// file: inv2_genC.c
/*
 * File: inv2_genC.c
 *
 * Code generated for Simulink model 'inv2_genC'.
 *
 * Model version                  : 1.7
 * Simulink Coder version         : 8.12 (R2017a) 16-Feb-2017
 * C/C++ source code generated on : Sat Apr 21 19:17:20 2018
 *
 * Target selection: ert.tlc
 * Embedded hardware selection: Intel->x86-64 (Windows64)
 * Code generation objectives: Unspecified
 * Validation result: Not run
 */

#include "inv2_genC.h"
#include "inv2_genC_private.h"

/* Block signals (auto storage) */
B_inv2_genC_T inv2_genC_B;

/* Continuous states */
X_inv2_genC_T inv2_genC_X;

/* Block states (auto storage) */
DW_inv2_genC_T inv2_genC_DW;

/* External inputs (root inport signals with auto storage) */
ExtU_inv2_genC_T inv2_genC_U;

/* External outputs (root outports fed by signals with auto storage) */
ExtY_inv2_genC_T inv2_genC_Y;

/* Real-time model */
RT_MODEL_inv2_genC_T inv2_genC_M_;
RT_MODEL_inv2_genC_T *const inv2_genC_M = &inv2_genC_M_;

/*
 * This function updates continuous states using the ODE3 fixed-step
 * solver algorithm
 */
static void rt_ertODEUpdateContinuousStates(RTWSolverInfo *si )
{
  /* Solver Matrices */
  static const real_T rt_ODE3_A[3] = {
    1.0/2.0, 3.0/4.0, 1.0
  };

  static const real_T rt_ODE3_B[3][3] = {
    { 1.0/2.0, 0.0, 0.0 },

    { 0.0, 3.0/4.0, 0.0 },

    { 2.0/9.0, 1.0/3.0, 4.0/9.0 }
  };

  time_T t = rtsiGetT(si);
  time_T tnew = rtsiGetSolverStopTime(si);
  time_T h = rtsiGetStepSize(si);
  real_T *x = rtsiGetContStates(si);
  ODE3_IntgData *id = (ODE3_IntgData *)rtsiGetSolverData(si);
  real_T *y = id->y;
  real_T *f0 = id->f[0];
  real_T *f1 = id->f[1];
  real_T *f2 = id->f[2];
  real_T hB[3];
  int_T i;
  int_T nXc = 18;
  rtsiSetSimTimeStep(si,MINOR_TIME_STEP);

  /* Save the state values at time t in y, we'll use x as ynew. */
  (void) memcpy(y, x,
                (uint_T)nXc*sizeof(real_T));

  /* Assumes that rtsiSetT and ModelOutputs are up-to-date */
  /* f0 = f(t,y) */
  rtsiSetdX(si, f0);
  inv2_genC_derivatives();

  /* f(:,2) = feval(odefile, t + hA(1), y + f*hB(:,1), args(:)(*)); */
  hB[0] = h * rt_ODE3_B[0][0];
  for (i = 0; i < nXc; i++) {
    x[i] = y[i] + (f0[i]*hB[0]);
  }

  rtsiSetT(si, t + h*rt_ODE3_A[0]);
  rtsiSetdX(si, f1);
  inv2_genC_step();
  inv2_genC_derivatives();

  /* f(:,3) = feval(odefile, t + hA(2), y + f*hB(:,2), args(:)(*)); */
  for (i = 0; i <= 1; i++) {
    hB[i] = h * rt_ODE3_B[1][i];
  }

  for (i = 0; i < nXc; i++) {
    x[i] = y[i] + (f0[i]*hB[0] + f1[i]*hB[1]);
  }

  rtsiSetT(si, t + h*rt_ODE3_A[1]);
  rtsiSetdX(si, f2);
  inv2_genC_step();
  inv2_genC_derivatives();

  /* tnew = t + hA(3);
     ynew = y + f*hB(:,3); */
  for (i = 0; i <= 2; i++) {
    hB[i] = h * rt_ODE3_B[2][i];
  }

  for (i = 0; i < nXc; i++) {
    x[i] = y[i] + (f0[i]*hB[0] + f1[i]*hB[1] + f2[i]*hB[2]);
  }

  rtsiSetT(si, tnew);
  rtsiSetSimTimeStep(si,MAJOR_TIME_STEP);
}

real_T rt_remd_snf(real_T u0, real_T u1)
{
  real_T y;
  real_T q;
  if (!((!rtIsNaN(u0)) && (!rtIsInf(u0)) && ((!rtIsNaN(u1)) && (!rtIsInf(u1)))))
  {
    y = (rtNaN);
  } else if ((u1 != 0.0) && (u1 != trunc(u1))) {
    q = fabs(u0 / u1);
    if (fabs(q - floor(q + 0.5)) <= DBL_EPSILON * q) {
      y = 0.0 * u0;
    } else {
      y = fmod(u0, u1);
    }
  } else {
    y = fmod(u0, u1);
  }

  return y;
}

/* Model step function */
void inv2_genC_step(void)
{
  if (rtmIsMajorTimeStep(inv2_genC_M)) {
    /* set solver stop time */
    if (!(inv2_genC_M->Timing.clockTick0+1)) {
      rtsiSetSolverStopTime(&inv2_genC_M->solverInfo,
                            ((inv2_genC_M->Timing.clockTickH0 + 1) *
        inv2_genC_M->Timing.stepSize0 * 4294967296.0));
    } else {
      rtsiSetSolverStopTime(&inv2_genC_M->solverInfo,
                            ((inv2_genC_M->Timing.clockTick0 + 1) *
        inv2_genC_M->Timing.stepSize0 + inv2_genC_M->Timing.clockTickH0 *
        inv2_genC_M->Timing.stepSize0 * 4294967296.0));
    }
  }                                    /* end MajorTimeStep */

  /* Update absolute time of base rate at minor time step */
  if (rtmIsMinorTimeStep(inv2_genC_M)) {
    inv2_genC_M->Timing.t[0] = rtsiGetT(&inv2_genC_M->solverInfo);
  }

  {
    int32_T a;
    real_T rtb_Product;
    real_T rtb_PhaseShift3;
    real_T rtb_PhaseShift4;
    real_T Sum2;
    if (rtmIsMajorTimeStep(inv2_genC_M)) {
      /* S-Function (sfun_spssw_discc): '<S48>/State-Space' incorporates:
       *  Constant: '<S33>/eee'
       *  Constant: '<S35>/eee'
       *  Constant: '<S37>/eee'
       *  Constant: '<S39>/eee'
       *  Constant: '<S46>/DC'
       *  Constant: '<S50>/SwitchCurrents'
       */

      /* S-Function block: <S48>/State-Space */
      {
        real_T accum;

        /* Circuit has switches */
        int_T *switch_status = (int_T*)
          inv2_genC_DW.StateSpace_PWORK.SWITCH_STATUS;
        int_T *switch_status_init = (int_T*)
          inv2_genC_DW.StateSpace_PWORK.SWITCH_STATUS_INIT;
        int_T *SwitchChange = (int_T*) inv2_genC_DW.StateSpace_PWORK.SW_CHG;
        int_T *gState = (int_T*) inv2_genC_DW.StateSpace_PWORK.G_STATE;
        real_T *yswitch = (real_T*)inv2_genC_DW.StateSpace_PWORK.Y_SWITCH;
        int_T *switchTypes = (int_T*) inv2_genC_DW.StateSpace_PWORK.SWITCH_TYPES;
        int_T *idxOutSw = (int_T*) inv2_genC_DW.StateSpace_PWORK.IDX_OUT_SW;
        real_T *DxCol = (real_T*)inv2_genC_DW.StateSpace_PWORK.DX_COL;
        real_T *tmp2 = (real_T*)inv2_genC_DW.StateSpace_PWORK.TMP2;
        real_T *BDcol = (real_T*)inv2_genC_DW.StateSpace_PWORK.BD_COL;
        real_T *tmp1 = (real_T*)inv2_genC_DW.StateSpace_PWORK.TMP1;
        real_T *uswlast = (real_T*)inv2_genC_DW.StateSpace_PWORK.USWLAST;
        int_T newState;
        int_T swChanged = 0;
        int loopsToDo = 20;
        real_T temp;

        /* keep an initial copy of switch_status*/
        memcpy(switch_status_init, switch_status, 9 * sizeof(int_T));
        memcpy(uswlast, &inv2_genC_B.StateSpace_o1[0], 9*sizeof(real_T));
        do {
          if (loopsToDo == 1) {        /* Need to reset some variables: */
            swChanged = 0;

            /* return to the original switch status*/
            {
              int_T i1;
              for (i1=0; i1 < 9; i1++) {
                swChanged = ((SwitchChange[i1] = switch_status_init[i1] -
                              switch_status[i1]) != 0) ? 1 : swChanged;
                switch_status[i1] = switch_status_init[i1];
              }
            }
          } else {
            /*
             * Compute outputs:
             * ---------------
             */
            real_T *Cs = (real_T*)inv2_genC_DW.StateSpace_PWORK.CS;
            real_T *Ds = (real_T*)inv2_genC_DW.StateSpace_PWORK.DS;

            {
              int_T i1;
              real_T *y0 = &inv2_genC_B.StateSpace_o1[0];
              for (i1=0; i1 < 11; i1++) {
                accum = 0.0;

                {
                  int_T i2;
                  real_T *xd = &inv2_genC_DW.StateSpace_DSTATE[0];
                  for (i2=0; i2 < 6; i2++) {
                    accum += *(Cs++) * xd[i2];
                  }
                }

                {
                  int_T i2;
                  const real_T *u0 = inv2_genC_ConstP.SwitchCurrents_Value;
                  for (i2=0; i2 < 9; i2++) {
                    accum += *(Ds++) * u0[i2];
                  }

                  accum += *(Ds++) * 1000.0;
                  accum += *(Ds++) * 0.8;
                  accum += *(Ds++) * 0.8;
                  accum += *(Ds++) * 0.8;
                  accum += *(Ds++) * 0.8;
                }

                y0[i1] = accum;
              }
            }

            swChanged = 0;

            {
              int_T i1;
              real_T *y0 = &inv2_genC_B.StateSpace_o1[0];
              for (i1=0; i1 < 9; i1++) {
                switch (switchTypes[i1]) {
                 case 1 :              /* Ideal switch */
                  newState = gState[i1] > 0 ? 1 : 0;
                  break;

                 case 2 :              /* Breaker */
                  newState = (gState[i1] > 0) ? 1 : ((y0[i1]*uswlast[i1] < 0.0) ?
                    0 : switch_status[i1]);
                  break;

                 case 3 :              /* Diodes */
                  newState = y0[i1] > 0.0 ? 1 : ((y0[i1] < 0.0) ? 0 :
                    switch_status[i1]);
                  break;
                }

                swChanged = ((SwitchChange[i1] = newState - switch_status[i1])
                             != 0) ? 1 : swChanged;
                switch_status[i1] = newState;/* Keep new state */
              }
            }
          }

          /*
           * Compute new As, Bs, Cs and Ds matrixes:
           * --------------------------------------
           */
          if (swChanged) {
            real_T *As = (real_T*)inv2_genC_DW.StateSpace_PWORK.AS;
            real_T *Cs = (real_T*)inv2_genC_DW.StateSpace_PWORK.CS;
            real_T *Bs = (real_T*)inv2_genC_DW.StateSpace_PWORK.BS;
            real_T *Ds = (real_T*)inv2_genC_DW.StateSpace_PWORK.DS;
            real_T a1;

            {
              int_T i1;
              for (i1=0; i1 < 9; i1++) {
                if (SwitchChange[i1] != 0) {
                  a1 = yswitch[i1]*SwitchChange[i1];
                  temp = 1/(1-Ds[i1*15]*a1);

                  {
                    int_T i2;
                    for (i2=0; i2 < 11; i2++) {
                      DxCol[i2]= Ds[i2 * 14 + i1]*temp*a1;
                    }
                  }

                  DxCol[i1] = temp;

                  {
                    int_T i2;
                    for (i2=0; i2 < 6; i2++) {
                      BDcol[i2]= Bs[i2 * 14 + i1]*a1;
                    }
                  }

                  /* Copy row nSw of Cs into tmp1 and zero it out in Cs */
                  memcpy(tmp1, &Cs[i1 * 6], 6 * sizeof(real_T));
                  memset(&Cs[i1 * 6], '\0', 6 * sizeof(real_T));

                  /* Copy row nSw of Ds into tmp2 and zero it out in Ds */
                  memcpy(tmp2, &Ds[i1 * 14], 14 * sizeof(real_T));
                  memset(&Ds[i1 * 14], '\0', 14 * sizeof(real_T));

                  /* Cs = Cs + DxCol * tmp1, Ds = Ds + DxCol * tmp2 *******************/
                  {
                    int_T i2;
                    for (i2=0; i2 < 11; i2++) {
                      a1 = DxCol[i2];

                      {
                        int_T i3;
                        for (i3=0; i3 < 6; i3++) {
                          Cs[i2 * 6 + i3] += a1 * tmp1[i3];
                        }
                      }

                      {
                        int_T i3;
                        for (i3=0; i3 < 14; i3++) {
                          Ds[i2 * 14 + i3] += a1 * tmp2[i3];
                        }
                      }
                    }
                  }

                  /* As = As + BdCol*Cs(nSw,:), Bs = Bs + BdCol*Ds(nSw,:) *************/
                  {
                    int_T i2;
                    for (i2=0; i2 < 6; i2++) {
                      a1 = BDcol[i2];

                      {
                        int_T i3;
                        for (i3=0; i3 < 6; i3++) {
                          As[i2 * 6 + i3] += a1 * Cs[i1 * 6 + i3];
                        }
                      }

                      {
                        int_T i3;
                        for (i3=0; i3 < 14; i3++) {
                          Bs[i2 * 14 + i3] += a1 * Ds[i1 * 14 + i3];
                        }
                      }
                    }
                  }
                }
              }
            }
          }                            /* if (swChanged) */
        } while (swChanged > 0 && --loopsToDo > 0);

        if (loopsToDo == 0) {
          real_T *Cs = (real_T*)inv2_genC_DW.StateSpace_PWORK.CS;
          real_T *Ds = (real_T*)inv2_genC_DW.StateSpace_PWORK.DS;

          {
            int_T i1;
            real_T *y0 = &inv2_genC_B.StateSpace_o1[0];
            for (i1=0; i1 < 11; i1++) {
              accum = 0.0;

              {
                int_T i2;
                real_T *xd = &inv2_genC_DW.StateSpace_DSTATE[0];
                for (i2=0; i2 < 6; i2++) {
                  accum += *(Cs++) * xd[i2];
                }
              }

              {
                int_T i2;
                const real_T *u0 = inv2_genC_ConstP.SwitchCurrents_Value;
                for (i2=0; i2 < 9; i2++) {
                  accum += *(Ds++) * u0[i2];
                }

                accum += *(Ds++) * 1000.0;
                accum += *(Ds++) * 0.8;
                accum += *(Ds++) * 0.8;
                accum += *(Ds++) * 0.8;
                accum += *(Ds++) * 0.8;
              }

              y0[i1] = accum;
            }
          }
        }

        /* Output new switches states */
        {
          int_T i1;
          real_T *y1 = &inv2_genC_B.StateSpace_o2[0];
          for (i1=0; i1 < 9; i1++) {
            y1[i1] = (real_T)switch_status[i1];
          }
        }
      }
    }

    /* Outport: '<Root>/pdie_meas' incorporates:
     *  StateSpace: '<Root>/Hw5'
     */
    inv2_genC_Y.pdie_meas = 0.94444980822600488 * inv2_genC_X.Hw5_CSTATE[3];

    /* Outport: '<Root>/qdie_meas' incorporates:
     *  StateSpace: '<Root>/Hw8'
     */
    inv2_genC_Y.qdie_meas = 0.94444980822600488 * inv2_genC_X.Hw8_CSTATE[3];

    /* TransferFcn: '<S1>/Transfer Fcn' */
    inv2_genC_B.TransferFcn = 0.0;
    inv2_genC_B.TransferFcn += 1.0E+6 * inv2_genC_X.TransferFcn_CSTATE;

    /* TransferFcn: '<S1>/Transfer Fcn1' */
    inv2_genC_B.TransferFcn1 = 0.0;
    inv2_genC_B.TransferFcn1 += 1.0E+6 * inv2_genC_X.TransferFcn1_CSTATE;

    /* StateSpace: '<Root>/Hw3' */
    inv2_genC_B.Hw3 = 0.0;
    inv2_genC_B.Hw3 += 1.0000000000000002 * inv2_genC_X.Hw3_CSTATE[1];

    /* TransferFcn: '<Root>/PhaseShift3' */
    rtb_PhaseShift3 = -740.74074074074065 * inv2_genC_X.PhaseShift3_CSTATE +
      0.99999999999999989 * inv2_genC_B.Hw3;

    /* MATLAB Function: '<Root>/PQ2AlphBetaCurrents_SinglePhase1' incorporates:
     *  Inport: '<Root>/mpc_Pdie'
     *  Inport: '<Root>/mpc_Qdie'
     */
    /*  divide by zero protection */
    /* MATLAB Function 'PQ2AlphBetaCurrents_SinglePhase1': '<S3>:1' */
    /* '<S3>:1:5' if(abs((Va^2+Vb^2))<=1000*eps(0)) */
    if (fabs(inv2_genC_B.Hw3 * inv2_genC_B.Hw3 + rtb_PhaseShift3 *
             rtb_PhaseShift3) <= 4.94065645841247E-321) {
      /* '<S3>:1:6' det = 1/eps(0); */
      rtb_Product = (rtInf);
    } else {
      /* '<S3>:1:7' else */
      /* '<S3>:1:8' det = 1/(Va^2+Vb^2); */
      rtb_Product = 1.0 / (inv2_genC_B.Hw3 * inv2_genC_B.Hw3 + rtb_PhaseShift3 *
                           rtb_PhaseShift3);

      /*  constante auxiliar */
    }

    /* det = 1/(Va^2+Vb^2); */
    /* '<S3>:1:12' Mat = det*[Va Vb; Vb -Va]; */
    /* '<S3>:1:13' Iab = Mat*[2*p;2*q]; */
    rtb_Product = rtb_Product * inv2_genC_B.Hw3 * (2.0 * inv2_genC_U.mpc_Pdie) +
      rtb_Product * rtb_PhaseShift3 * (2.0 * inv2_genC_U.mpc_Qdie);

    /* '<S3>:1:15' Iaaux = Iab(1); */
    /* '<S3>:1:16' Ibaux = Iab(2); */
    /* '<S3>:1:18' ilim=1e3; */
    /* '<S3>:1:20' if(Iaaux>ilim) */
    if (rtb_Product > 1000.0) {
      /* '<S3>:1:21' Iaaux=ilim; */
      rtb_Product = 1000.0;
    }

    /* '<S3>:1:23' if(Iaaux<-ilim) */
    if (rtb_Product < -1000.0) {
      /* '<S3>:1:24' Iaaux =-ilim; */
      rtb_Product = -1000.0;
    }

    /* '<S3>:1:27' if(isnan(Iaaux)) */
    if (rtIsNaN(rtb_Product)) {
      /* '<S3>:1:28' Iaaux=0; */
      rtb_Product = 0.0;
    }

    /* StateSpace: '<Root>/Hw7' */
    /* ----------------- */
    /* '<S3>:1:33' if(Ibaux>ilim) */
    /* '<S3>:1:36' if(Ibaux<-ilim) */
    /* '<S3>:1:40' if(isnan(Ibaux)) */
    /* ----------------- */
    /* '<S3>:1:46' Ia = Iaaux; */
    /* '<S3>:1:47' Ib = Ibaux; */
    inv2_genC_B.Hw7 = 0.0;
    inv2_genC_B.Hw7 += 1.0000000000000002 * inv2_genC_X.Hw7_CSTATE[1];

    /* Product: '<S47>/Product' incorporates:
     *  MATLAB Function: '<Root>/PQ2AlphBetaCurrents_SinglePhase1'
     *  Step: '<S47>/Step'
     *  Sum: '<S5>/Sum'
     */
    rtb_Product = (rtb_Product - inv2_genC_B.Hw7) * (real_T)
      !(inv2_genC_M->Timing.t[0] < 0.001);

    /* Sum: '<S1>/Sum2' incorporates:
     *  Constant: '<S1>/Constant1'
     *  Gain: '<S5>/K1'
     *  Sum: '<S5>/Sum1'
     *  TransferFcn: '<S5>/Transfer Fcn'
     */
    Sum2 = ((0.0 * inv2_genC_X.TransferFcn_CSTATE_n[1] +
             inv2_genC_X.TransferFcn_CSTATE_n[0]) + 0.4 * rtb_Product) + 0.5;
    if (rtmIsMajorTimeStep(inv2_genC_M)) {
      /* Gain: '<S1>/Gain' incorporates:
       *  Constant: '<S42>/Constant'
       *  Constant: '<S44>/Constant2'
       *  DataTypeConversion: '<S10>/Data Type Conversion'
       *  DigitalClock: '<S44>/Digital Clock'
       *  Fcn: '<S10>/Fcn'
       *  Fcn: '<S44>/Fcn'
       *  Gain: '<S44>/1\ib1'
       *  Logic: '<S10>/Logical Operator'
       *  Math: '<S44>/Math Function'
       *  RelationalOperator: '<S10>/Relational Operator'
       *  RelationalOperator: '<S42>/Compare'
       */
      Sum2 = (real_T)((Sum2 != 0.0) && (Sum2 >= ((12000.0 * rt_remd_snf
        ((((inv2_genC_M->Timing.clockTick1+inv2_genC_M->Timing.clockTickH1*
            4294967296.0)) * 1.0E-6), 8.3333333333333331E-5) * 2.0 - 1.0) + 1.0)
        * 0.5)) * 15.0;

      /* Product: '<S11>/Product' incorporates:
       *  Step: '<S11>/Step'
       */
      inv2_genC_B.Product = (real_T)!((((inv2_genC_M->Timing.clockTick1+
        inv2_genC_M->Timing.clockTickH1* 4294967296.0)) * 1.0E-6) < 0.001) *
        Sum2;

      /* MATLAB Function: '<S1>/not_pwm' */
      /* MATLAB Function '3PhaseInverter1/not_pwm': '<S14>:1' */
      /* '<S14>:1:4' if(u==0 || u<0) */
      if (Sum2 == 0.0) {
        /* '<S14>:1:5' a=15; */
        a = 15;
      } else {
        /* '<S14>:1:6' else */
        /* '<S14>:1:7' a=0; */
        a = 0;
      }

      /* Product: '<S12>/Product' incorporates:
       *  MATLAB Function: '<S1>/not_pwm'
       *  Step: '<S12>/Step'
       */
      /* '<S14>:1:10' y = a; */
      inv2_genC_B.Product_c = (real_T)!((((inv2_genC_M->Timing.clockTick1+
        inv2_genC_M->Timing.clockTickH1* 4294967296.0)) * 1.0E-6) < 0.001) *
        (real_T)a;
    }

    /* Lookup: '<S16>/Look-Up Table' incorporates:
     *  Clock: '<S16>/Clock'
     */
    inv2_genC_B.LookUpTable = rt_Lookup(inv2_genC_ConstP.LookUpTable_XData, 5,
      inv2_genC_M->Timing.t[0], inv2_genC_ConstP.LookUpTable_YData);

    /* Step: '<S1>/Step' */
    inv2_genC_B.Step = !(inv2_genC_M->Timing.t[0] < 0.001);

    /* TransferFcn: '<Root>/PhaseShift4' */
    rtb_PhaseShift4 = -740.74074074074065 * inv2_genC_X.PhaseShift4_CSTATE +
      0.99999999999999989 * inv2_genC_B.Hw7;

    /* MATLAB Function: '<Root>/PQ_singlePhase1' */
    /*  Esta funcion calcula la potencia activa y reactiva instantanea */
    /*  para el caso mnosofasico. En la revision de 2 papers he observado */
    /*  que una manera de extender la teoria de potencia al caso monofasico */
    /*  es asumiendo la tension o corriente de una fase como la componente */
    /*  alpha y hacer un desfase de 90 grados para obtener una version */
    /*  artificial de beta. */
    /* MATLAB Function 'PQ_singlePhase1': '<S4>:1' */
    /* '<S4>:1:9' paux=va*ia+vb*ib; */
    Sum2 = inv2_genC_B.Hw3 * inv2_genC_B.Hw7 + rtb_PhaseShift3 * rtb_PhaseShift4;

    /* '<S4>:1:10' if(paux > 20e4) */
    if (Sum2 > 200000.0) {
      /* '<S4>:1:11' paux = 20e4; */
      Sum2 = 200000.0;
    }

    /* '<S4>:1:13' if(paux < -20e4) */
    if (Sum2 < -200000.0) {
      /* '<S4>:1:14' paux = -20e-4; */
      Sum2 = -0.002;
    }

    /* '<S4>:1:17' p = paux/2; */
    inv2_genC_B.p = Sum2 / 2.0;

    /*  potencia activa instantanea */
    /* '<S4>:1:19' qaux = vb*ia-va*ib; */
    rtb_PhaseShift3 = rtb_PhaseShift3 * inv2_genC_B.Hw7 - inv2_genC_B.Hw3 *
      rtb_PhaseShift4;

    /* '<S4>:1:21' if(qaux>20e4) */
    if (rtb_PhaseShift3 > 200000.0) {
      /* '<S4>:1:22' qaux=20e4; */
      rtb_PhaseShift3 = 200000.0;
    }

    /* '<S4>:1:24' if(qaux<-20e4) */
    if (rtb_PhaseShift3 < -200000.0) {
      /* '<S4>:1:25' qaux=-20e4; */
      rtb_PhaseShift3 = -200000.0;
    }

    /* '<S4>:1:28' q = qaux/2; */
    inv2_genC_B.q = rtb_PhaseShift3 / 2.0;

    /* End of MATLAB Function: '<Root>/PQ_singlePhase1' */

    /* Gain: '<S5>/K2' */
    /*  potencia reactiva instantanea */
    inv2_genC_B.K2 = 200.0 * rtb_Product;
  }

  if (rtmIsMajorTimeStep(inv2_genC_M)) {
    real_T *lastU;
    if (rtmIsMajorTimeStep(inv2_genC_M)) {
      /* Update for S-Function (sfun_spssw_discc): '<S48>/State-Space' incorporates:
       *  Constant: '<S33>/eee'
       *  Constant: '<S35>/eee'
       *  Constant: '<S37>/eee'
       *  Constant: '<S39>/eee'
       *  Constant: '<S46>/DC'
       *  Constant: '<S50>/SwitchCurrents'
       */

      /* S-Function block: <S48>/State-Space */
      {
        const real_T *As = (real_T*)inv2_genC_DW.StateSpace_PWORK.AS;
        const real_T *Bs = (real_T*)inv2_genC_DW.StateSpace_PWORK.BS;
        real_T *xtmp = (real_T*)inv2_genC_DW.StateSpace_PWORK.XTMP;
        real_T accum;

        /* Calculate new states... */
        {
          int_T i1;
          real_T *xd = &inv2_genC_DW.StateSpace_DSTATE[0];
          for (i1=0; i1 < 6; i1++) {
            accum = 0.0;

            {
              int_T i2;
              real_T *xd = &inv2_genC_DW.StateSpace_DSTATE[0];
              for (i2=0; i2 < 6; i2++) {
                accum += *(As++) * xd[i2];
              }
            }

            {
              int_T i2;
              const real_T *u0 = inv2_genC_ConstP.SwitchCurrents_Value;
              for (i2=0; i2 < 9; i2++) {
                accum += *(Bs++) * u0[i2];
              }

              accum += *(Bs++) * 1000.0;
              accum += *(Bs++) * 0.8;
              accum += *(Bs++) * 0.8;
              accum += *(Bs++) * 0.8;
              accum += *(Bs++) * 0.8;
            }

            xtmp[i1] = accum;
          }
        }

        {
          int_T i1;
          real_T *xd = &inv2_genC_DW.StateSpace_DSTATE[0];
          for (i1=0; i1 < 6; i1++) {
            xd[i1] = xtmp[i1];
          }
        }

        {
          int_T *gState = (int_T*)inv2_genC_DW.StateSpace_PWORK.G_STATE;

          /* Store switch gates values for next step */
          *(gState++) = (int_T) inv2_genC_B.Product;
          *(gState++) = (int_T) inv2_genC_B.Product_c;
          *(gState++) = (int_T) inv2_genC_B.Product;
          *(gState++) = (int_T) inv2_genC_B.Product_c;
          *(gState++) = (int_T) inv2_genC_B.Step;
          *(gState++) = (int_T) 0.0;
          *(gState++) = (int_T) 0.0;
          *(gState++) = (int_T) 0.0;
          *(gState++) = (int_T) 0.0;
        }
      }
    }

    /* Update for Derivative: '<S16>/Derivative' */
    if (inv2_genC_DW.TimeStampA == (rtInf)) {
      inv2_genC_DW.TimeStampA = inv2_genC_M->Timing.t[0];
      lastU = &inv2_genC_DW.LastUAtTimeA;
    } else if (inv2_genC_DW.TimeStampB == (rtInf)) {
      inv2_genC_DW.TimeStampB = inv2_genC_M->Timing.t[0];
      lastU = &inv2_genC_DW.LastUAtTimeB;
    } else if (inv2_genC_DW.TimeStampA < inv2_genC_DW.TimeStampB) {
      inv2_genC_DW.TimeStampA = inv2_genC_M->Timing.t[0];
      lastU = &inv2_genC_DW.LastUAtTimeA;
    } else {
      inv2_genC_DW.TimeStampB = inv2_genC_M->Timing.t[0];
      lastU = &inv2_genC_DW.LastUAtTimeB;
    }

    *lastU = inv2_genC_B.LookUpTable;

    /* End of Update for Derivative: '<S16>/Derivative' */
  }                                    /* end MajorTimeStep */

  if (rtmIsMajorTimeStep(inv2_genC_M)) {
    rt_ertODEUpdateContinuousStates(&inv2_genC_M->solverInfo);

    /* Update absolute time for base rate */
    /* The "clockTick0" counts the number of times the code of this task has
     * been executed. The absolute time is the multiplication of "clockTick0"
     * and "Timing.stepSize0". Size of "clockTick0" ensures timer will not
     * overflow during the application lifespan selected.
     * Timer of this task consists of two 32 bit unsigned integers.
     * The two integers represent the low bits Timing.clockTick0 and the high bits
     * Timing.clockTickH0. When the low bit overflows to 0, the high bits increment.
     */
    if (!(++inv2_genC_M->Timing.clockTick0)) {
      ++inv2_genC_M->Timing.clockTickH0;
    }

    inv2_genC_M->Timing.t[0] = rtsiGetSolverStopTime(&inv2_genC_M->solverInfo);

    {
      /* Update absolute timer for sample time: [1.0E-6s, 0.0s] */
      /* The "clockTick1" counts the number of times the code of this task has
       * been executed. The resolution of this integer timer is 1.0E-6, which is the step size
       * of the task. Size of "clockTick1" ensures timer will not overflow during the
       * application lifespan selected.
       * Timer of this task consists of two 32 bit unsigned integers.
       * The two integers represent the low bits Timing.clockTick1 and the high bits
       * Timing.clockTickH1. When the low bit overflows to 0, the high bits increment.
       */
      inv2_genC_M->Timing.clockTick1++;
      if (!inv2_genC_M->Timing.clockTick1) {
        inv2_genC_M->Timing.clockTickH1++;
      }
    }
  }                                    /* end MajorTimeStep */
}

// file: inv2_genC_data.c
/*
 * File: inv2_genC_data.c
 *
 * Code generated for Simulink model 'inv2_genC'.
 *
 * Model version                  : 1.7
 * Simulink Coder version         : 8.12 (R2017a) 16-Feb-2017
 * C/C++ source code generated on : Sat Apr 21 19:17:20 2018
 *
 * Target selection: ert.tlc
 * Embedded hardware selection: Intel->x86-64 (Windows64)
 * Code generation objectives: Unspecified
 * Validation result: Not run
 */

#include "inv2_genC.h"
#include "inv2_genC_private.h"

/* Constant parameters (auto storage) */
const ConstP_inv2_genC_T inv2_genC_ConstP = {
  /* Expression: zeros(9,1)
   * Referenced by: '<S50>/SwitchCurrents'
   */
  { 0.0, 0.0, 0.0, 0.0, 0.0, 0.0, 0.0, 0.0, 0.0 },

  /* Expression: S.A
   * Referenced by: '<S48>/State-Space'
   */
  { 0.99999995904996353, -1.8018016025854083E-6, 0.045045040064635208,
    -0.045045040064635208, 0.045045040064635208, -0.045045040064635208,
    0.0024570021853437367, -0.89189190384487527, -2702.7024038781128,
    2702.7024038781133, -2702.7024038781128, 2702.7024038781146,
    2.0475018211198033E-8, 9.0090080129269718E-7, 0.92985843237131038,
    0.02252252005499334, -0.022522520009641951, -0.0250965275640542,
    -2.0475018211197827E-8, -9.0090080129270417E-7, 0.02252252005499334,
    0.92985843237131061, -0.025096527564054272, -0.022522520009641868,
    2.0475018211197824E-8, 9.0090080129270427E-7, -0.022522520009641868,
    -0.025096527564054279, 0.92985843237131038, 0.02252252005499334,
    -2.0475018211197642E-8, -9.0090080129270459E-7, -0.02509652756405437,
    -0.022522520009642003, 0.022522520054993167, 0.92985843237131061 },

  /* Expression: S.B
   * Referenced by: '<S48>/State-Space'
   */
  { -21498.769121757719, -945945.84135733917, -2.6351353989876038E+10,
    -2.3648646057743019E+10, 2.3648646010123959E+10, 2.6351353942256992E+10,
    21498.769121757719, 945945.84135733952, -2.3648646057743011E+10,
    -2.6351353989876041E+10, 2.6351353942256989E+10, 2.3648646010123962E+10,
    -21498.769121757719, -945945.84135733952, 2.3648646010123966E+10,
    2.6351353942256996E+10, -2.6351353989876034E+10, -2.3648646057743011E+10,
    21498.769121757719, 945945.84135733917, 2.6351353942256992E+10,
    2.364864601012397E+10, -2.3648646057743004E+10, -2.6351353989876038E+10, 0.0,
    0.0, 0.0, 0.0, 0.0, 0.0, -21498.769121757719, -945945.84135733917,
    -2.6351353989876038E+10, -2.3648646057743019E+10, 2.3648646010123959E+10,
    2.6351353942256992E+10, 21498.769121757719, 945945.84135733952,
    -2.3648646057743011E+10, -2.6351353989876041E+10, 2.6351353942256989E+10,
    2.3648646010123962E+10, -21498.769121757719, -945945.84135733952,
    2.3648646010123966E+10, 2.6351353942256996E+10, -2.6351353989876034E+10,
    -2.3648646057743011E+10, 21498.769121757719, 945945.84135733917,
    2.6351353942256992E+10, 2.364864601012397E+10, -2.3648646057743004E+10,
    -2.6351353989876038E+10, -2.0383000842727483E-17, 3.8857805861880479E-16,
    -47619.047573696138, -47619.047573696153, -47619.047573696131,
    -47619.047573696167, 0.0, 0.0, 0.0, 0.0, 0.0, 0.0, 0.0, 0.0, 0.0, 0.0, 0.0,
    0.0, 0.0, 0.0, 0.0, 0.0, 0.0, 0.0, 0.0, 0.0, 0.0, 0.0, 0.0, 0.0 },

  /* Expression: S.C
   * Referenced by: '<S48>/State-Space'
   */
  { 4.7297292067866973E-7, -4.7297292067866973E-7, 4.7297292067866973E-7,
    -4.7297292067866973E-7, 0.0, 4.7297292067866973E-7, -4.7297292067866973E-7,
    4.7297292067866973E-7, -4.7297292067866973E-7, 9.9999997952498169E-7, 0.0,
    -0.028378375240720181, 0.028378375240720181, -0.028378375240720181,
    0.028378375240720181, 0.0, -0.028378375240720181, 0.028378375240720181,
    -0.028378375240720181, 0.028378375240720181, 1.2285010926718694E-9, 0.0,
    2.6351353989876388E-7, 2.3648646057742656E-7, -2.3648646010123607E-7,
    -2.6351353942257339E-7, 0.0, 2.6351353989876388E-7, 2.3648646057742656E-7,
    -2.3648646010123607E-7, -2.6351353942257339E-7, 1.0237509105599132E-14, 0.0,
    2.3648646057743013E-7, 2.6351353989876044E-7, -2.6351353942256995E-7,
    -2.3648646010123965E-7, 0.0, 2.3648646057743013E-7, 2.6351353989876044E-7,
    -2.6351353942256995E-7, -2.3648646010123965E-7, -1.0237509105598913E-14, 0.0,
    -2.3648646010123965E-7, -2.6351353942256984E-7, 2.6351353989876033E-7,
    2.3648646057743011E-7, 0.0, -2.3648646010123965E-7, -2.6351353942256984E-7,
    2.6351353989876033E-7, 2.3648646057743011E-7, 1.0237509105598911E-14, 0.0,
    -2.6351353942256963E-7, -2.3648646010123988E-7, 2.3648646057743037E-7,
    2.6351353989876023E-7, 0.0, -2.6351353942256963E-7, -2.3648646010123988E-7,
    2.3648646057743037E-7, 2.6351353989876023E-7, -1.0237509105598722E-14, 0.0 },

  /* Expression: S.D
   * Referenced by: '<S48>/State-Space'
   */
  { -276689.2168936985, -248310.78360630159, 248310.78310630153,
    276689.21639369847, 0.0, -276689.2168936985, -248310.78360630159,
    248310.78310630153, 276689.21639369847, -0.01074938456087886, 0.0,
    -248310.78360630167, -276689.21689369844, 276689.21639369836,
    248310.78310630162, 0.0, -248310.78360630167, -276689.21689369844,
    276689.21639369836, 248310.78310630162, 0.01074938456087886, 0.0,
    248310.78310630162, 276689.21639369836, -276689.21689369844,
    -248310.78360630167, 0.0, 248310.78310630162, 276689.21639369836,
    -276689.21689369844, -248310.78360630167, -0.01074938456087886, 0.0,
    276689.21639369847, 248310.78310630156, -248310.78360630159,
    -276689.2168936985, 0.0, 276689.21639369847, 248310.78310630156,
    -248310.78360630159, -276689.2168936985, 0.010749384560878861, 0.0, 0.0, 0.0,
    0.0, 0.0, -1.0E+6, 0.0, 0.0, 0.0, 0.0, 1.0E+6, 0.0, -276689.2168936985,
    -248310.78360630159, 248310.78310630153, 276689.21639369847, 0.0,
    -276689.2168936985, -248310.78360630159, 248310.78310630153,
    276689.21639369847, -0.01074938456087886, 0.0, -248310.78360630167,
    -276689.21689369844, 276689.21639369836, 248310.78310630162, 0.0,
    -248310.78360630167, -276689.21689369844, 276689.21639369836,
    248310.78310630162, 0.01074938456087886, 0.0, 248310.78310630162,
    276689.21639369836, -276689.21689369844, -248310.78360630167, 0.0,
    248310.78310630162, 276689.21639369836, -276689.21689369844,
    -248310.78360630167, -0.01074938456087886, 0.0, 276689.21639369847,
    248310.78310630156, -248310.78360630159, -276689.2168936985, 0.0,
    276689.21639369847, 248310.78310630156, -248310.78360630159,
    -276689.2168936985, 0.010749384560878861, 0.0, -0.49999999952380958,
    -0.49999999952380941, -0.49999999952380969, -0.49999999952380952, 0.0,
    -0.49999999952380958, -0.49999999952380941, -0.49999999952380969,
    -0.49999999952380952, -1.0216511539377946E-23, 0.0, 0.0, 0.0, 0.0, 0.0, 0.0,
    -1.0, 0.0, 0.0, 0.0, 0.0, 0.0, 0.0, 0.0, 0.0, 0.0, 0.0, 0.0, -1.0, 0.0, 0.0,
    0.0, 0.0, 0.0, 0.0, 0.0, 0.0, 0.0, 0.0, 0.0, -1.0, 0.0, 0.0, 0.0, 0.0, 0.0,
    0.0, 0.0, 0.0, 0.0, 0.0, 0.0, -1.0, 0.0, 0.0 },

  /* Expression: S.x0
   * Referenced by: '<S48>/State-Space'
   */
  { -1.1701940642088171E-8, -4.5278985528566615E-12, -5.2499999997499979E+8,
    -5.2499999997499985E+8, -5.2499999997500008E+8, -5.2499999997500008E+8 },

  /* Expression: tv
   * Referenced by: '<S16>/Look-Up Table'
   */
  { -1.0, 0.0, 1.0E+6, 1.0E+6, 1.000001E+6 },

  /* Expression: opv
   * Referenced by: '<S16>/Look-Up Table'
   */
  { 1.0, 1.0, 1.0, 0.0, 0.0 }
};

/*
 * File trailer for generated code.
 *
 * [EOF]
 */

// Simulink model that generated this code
simulink model "inv2_genC"  (R2017a)
settings: Solver=ode3  StartTime=0.0  StopTime=10.0  FixedStep=1e-6  MaxStep=1e-4  RelTol=1e-3
libraries: powerlib x17, dsparch4 x4, powerlib_meascontrol x1

== system inv2_genC ==
  note: DIESEL - CSI
  mpc_Pdie : Inport
  mpc_Qdie : Inport  Port=2
  3PhaseInverter1 : Subsystem  mask{st_time=1e-3, f_sw=12000, samp_f=1e-6}
      mask prompts: st_time "Tiempo muerto (Start)"; f_sw "Switching frequency"; samp_f "Sampling frequency"
  DC_2 : powerlib/Electrical Sources/DC Voltage Source  Amplitude=1000  Measurements=None
  Ground3 : powerlib/Elements/Ground  LConnTagsString=a
  Hw3 : dsparch4/Analog Filter Design  method=Bessel  filttype=Lowpass  N=2  Wlo=7000*2*pi  Whi=80  Rp=2  Rs=80
  Hw5 : dsparch4/Analog Filter Design  method=Bessel  filttype=Lowpass  N=4  Wlo=30*2*pi  Whi=80  Rp=2  Rs=80
  Hw7 : dsparch4/Analog Filter Design  method=Bessel  filttype=Lowpass  N=2  Wlo=7000*2*pi  Whi=80  Rp=2  Rs=80
  Hw8 : dsparch4/Analog Filter Design  method=Bessel  filttype=Lowpass  N=4  Wlo=30*2*pi  Whi=80  Rp=2  Rs=80
  PQ2AlphBetaCurrents_SinglePhase1 : MATLAB Function  TreatAsAtomicUnit=on
  PQ_singlePhase1 : MATLAB Function  TreatAsAtomicUnit=on
  PR Controller_0_ref 2 : Subsystem  mask{Kp=40/100, Ki=200, wa=2, w0=60*2*pi, st_time=1e-3}
      mask prompts: Kp "Ganancia Proporcional"; Ki "Ganancia Integral"; wa "Ancho camapana resonancia"; w0 "Frecuencia Central"; st_time "Tiempo muerto (Start)"
  PhaseShift3 : TransferFcn  Numerator=[2.7e-3 -1]  Denominator=[2.7e-3 1]
  PhaseShift4 : TransferFcn  Numerator=[2.7e-3 -1]  Denominator=[2.7e-3 1]
  Rin1 : powerlib/Elements/Series RLC Branch  LConnTagsString=__new0  RConnTagsString=__new0  BranchType=R  Resistance=.001  Inductance=0  SetiL0=off  InitialCurrent=0  Capacitance=0  Setx0=off  InitialVoltage=0  Measurements=None
  Scope1 : Scope  NumInputPorts=2
  Scope3 : Scope  NumInputPorts=2
  powergui : powerlib/powergui  Priority=1  SimulationMode=Discrete  SampleTime=1e-6  frequency=60  Iterations=50  frequencyindice=0  Pbase=100e6  ErrMax=1e-4  UnitsV=kV  UnitsW=MW  buscounter=0  FunctionMessages=off  echomessages=off  EnableUseOfTLC=off  CurrentSourceSwitches=off  DisableSnubberDevices=off  DisableRonSwitches=off  DisableVfSwitches=off  DisplayEquations=off  SolverType=Tustin/Backward Euler (TBE)  Interpol=off  ExternalGateDelay=off  methode=off  Ts=100  x0status=blocks  SPID=on  SwTol=0  HookPort=off  RestoreLinks=warning  ResistiveCurrentMeasurement=off  Frange=[0:2:500]  Ylog=off  Xlog=on  ShowGrid=off  save=off  variable=ZData  structure=0  ZoomFFT=off  StartTime=0.0  cycles=1  DisplayStyle=1  fundamental=60  FreqAxis=off  MaxFrequency=1000  frequencyindicesteady=1  RmsSteady=1  display=off
  pdie_meas : Outport
  qdie_meas : Outport  Port=2
  wires:
  3PhaseInverter1/1(Iout) -> Hw7/1
  [D_die] -> 3PhaseInverter1/1(A_in)
  PQ2AlphBetaCurrents_SinglePhase1/1(Ia) -> [Ia_ref_die]
  [I_die] -> PhaseShift4/1, [I_alf_die]
  Hw7/1 -> [I_die]
  [V_alf_die] -> PQ2AlphBetaCurrents_SinglePhase1/1(Va)
  PhaseShift4/1 -> [I_bet_die]
  PhaseShift3/1 -> [V_bet_die]
  [Ia_ref_die] -> PR Controller_0_ref 2/1(ref), Scope1/1
  [V_die] -> Scope3/2
  Hw3/1 -> [V_die]
  3PhaseInverter1/2(Vout) -> Hw3/1
  [I_die] -> PR Controller_0_ref 2/2(real), Scope1/2
  PR Controller_0_ref 2/1(Out1) -> [D_die]
  [V_die] -> [V_alf_die], PhaseShift3/1
  [I_die] -> Scope3/1
  [V_bet_die] -> PQ2AlphBetaCurrents_SinglePhase1/2(Vb)
  PQ_singlePhase1/1(p) -> Hw5/1
  PQ_singlePhase1/2(q) -> Hw8/1
  [I_bet_die] -> PQ_singlePhase1/4(ib)
  [V_bet_die] -> PQ_singlePhase1/2(vb)
  [V_alf_die] -> PQ_singlePhase1/1(va)
  Hw8/1 -> qdie_meas/1
  [I_alf_die] -> PQ_singlePhase1/3(ia)
  Hw5/1 -> pdie_meas/1
  mpc_Pdie/1 -> PQ2AlphBetaCurrents_SinglePhase1/3(p)
  mpc_Qdie/1 -> PQ2AlphBetaCurrents_SinglePhase1/4(q)
  connections:
  DC_2/RConn1 -- Rin1/LConn1
  3PhaseInverter1/RConn2 -- Ground3/LConn1
  Rin1/RConn1 -- 3PhaseInverter1/LConn1
  DC_2/LConn1 -- 3PhaseInverter1/LConn2

== system inv2_genC/3PhaseInverter1 ==
  note: Gate Drivers: Generan las señales cuadradas para
      | la conmutacion del convertidor de 3 brazos e implementan el
      | tiempo muerto para mejorar la calidad de la simulacion
  A_in : Inport
  Breaker : powerlib/Elements/Breaker  InitialState=0  SwitchingTimes="[1/60  5/60]"  External=on  BreakerResistance=0.01  SnubberResistance=1e6  SnubberCapacitance=inf  Measurements=None  MoreParameters=on  NoBreakLoop=off
  Cf : powerlib/Elements/Series RLC Branch  LConnTagsString=__new0  RConnTagsString=__new0  BranchType=C  Resistance=1  Inductance=1e-3  SetiL0=off  InitialCurrent=0  Capacitance=22e-6  Setx0=off  InitialVoltage=0  Measurements=None
  Constant1 : Constant  Value=0.5
  Gain : Gain  Gain=15
  H bridge : Subsystem
  I sens A : powerlib/Measurements/Current Measurement  PhasorSimulation=off  OutputType=Complex  PSBequivalent=0
  Lf : powerlib/Elements/Series RLC Branch  LConnTagsString=__new0  RConnTagsString=__new0  BranchType=RL  Resistance=.1  Inductance=30e-3  SetiL0=off  InitialCurrent=0  Capacitance=1e-6  Setx0=off  InitialVoltage=0  Measurements=None
  PWM Generator (DC-DC) : powerlib_meascontrol/Pulse & Signal Generators/PWM Generator (DC-DC)  Fsw=f_sw  Ts=samp_f
  Step : Step  Time=st_time  SampleTime=0
  Steper1 : Subsystem
  Steper3 : Subsystem
  Sum2 : Sum
  Transfer Fcn : TransferFcn  Denominator=[1e-6 1]
  Transfer Fcn1 : TransferFcn  Denominator=[1e-6 1]
  Vsensa1 : powerlib/Measurements/Voltage Measurement  PhasorSimulation=off  OutputType=Complex  PSBequivalent=0
  not_pwm : MATLAB Function  TreatAsAtomicUnit=on
  Vout+ : PMIOPort  Port=1  Side=Right
  Vout- : PMIOPort  Port=2  Side=Right
  Collector : PMIOPort  Port=3  Side=Left
  Emitter : PMIOPort  Port=4  Side=Left
  Iout : Outport
  Vout : Outport  Port=2
  wires:
  Vsensa1/1 -> Transfer Fcn1/1  "A_volts"
  I sens A/1 -> Transfer Fcn/1  "A_current"
  [pwma] -> H bridge/4(Blo)
  [Npwma] -> H bridge/3(Alo), H bridge/2(Bhi)
  [pwma] -> H bridge/1(Ahi)
  Gain/1 -> not_pwm/1(u), Steper1/1(In1)
  Steper3/1(Out1) -> [Npwma]
  Steper1/1(Out1) -> [pwma]
  A_in/1 -> Sum2/1
  Constant1/1 -> Sum2/2
  PWM Generator (DC-DC)/1 -> Gain/1
  Sum2/1 -> PWM Generator (DC-DC)/1
  not_pwm/1(y) -> Steper3/1(In1)
  Transfer Fcn/1 -> Iout/1
  Transfer Fcn1/1 -> Vout/1
  Step/1 -> Breaker/1
  connections:
  Cf/RConn1 -- Vsensa1/LConn2 -- Vout-/RConn1 -- H bridge/RConn2
  Lf/LConn1 -- H bridge/RConn1
  H bridge/RConn4 -- Emitter/RConn1
  H bridge/RConn3 -- Collector/RConn1
  Breaker/LConn1 -- I sens A/RConn1
  Breaker/RConn1 -- Vsensa1/LConn1 -- Vout+/RConn1
  Lf/RConn1 -- I sens A/LConn1 -- Cf/LConn1

== system inv2_genC/PR Controller_0_ref 2 ==
  ref : Inport
  real : Inport  Port=2
  K1 : Gain  Gain=Kp
  K2 : Gain  Gain=Ki
  Steper6 : Subsystem
  Sum : Sum  Inputs=+-
  Sum1 : Sum  Inputs=+|+
  Transfer Fcn : TransferFcn  Numerator=[1 0]  Denominator=[1 wa (w0)^2]
  Out1 : Outport
  wires:
  real/1 -> Sum/2
  ref/1 -> Sum/1
  Sum/1 -> Steper6/1(In1)
  K1/1 -> Sum1/1
  Transfer Fcn/1 -> Sum1/2
  K2/1 -> Transfer Fcn/1
  Steper6/1(Out1) -> K1/1, K2/1
  Sum1/1 -> Out1/1

== system inv2_genC/3PhaseInverter1/H bridge ==
  note: Convertirdor de 3 brazos:
      |
      | Implementado usando interruptores
      | ideales para agilizar la simulacion.
      | la salida E correspone a la corriente y laa
      | tension de cada componente
      | (sea interruptor o diodo) y su respectiva
      | corriente. no tienen puerto de salida ya que no
      | son relevantes para lo que se desea simular.
      |
      | si g=0 interruptor no conduce.
      | si g=1 interruptor conduce.
      |
      | conmutacion ocurre instantaneamente sin
      | retardo.
  Ahi : Inport
  Bhi : Inport  Port=2
  Alo : Inport  Port=3
  Blo : Inport  Port=4
   sw_ahi{1..2,5..6} (4 alike) : powerlib/Power Electronics/Ideal Switch  Ron=0.1  Lon=0  IC=0  Rs=1e6  Cs=10e-12  Measurements=on
  Diode{1..3,6} (4 alike) : powerlib/Power Electronics/Diode  Ron=.2  Lon=0  Vf=0.8  IC=0  UseSnubber=0  Rs=0  Cs=0  Measurements=on
  " Vout+" : PMIOPort  Tag=PMCPort  Port=1  Side=Right
  Vout- : PMIOPort  Tag=PMCPort  Port=2  Side=Right
  Collector : PMIOPort  Tag=PMCPort  Port=3  Side=Right
  Emitter : PMIOPort  Tag=PMCPort  Port=4  Side=Right
  wires:
  Bhi/1 -> " sw_ahi2"/1
  Blo/1 -> " sw_ahi5"/1
  Ahi/1 -> " sw_ahi1"/1
  Alo/1 -> " sw_ahi6"/1
  connections:
  " sw_ahi1"/LConn1 -- Diode1/LConn1 -- " Vout+"/RConn1 -- Diode6/RConn1 -- " sw_ahi6"/RConn1
  " sw_ahi2"/RConn1 -- Diode1/RConn1 -- " sw_ahi1"/RConn1 -- Collector/RConn1 -- Diode2/RConn1
  " sw_ahi5"/LConn1 -- " sw_ahi6"/LConn1 -- Diode6/LConn1 -- Emitter/RConn1 -- Diode3/LConn1
  " sw_ahi5"/RConn1 -- Diode2/LConn1 -- " sw_ahi2"/LConn1 -- Vout-/RConn1 -- Diode3/RConn1

== system inv2_genC/3PhaseInverter1/Steper1 ==
  In1 : Inport
  Product : Product
  Step : Step  Time=st_time  SampleTime=samp_f
  Out1 : Outport
  wires:
  Product/1 -> Out1/1
  In1/1 -> Product/1
  Step/1 -> Product/2

== system inv2_genC/3PhaseInverter1/Steper3 ==
  In1 : Inport
  Product : Product
  Step : Step  Time=st_time  SampleTime=samp_f
  Out1 : Outport
  wires:
  Step/1 -> Product/2
  In1/1 -> Product/1
  Product/1 -> Out1/1

== system inv2_genC/PR Controller_0_ref 2/Steper6 ==
  In1 : Inport
  Product : Product
  Step : Step  Time=st_time  SampleTime=0
  Out1 : Outport
  wires:
  Product/1 -> Out1/1
  In1/1 -> Product/1
  Step/1 -> Product/2

== matlab function inv2_genC/3PhaseInverter1/not_pwm ==
function y = fcn(u)
%#codegen

if(u==0 || u<0)
    a=15;
else
    a=0;
end;

y = a;

== matlab function inv2_genC/PQ2AlphBetaCurrents_SinglePhase1 ==
function [Ia, Ib] = fcn(Va, Vb, p, q)
%#codegen

% divide by zero protection
if(abs((Va^2+Vb^2))<=1000*eps(0))
    det = 1/eps(0);
else
    det = 1/(Va^2+Vb^2); % constante auxiliar
end;
%det = 1/(Va^2+Vb^2);

Mat = det*[Va Vb; Vb -Va];
Iab = Mat*[2*p;2*q];

Iaaux = Iab(1);
Ibaux = Iab(2);

ilim=1e3;

if(Iaaux>ilim)
    Iaaux=ilim;
end;
if(Iaaux<-ilim)
    Iaaux =-ilim;    
end;

if(isnan(Iaaux))
    Iaaux=0;
end;
%-----------------

if(Ibaux>ilim)
    Ibaux=ilim;
end;
if(Ibaux<-ilim)
    Ibaux =-ilim;    
end;

if(isnan(Ibaux))
    Ibaux=0;
end;
%-----------------

Ia = Iaaux;
Ib = Ibaux;

== matlab function inv2_genC/PQ_singlePhase1 ==
function [p, q] = fcn(va, vb, ia, ib)
% Esta funcion calcula la potencia activa y reactiva instantanea
% para el caso mnosofasico. En la revision de 2 papers he observado
% que una manera de extender la teoria de potencia al caso monofasico
% es asumiendo la tension o corriente de una fase como la componente
% alpha y hacer un desfase de 90 grados para obtener una version
% artificial de beta.

paux=va*ia+vb*ib;
if(paux > 20e4)
    paux = 20e4;
end
if(paux < -20e4)
    paux = -20e-4;
end

p = paux/2; % potencia activa instantanea

qaux = vb*ia-va*ib;

if(qaux>20e4)
    qaux=20e4;
end
if(qaux<-20e4)
    qaux=-20e4;
end

q = qaux/2; % potencia reactiva instantanea
